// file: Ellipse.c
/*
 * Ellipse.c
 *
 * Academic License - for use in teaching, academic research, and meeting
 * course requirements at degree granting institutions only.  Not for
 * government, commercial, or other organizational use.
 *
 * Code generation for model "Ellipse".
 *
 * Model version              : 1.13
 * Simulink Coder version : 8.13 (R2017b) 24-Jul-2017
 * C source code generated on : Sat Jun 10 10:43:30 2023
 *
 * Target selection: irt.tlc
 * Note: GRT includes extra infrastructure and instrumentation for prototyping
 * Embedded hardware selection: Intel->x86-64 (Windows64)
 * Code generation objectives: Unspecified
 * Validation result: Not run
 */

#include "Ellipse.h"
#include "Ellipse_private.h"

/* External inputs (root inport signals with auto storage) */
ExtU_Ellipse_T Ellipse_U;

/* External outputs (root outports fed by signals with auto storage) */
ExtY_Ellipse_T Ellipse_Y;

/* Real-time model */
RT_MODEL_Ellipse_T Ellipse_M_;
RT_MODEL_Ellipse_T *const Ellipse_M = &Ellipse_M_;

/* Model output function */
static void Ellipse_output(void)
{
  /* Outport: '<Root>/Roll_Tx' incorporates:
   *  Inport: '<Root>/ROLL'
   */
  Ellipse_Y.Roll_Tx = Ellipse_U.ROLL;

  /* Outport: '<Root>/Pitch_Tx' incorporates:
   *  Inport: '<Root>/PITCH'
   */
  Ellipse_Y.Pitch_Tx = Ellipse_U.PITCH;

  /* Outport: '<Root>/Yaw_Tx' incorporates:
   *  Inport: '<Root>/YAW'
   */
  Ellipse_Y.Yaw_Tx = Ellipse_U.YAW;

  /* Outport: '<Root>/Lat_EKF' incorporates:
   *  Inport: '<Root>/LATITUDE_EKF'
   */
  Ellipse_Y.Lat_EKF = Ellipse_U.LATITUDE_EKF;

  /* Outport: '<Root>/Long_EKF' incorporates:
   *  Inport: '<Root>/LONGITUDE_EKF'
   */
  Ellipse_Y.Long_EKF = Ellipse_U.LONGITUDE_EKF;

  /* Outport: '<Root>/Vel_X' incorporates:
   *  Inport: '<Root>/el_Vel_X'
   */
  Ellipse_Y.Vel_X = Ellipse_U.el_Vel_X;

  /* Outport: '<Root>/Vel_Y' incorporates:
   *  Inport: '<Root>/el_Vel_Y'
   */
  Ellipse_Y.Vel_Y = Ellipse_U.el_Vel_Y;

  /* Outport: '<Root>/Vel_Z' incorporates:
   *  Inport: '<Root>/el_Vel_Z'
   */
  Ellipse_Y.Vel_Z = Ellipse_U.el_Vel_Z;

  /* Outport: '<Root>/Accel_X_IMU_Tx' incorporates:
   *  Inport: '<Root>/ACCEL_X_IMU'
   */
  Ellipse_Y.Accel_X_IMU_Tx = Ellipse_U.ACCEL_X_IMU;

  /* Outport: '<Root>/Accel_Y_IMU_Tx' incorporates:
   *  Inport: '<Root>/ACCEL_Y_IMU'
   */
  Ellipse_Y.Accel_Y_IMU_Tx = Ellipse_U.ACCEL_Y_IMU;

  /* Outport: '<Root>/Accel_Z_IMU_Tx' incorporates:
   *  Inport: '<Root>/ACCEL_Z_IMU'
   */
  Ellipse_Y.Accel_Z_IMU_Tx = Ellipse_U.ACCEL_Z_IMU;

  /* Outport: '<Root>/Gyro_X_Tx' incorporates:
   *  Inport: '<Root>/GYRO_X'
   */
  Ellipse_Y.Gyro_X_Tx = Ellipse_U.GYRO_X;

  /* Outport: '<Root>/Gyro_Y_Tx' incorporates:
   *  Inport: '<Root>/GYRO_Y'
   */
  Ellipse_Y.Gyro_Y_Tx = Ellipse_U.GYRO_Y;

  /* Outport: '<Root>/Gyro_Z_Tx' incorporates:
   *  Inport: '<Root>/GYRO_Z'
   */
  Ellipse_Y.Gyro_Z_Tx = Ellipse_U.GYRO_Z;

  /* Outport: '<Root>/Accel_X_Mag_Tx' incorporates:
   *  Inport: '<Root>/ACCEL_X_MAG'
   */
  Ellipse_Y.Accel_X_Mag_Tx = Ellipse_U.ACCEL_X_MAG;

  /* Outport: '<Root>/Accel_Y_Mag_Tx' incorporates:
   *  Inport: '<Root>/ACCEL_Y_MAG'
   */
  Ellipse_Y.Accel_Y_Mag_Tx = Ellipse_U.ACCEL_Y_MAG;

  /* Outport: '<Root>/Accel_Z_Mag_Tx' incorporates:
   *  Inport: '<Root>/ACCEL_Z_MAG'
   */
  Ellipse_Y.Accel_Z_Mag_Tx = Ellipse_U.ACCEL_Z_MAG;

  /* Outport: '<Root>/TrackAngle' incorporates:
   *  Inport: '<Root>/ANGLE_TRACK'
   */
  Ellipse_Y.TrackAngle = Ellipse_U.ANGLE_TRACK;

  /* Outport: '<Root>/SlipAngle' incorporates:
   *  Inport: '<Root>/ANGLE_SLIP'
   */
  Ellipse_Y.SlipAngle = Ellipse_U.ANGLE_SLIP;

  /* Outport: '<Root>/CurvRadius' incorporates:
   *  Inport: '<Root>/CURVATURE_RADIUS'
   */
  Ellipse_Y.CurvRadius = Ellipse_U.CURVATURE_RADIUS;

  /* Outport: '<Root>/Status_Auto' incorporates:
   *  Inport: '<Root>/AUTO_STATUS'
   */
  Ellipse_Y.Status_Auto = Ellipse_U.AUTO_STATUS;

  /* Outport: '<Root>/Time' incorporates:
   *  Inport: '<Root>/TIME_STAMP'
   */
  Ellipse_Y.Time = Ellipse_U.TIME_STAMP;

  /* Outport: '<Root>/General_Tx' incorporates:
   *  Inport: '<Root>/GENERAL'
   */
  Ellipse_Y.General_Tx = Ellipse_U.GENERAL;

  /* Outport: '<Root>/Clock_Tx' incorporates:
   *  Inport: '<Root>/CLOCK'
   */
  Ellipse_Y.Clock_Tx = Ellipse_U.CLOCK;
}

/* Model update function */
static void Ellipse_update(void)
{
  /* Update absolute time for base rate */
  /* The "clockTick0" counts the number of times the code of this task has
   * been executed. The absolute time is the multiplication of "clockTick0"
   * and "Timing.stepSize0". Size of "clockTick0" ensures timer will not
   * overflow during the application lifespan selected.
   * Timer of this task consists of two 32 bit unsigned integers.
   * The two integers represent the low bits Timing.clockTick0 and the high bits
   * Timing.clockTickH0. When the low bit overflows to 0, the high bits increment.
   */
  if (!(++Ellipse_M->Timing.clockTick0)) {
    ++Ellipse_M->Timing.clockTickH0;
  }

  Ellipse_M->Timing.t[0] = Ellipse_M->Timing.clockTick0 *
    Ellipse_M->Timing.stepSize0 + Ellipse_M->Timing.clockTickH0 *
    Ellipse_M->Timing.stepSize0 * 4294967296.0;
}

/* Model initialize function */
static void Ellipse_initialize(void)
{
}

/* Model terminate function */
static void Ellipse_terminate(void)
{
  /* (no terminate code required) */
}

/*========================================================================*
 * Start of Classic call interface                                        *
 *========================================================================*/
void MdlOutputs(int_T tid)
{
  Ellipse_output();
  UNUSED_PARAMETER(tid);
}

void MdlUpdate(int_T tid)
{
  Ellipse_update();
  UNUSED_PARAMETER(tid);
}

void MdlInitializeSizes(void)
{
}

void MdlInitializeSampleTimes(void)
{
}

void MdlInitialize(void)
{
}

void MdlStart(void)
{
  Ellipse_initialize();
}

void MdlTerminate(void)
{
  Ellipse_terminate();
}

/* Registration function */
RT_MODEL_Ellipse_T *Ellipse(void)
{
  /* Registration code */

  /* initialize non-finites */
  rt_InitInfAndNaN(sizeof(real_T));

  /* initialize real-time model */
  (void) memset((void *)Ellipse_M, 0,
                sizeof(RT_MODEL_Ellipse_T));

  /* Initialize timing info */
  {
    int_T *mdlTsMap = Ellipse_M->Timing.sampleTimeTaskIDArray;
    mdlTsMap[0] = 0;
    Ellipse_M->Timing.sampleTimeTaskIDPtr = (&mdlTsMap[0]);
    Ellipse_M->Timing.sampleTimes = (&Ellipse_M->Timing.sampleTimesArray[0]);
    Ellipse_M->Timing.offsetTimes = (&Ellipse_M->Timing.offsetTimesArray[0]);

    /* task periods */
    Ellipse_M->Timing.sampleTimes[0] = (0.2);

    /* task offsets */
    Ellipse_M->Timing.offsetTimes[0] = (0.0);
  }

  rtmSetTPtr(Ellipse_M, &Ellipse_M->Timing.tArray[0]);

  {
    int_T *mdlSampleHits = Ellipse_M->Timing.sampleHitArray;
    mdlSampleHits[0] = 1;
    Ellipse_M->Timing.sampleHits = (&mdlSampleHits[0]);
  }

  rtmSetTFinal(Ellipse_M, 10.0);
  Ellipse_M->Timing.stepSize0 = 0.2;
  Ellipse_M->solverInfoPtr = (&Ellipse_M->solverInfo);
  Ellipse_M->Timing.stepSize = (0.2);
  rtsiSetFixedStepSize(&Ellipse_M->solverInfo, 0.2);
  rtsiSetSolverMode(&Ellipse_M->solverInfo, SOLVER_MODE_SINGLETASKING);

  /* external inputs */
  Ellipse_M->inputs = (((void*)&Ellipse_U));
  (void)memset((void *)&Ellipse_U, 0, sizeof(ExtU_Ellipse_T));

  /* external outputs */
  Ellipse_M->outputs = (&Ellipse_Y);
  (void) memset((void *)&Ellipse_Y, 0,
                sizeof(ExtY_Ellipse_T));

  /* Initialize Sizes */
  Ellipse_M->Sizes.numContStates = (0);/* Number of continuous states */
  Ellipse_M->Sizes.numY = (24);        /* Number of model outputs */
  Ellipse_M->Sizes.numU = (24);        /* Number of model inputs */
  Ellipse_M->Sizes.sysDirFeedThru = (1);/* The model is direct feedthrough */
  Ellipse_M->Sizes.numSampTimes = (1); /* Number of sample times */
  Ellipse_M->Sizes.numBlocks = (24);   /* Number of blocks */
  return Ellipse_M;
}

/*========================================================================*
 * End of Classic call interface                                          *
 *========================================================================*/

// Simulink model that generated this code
simulink model "Ellipse"  (R2017b)
settings: Solver=FixedStepAuto  StartTime=0.0  StopTime=10.0  RelTol=1e-3

== system Ellipse ==
  ROLL : Inport
  PITCH : Inport  Port=2
  YAW : Inport  Port=3
  LATITUDE_EKF : Inport  Port=4
  LONGITUDE_EKF : Inport  Port=5
  el_Vel_X : Inport  Port=6
  el_Vel_Y : Inport  Port=7
  el_Vel_Z : Inport  Port=8
  ACCEL_X_IMU : Inport  Port=9
  ACCEL_Y_IMU : Inport  Port=10
  ACCEL_Z_IMU : Inport  Port=11
  GYRO_X : Inport  Port=12
  GYRO_Y : Inport  Port=13
  GYRO_Z : Inport  Port=14
  ACCEL_X_MAG : Inport  Port=15
  ACCEL_Y_MAG : Inport  Port=16
  ACCEL_Z_MAG : Inport  Port=17
  ANGLE_TRACK : Inport  Port=18
  ANGLE_SLIP : Inport  Port=19
  CURVATURE_RADIUS : Inport  Port=20
  AUTO_STATUS : Inport  Port=21
  TIME_STAMP : Inport  Port=22
  GENERAL : Inport  Port=23
  CLOCK : Inport  Port=24
  Roll_Tx : Outport
  Pitch_Tx : Outport  Port=2
  Yaw_Tx : Outport  Port=3
  Lat_EKF : Outport  Port=4
  Long_EKF : Outport  Port=5
  Vel_X : Outport  Port=6
  Vel_Y : Outport  Port=7
  Vel_Z : Outport  Port=8
  Accel_X_IMU_Tx : Outport  Port=9
  Accel_Y_IMU_Tx : Outport  Port=10
  Accel_Z_IMU_Tx : Outport  Port=11
  Gyro_X_Tx : Outport  Port=12
  Gyro_Y_Tx : Outport  Port=13
  Gyro_Z_Tx : Outport  Port=14
  Accel_X_Mag_Tx : Outport  Port=15
  Accel_Y_Mag_Tx : Outport  Port=16
  Accel_Z_Mag_Tx : Outport  Port=17
  TrackAngle : Outport  Port=18
  SlipAngle : Outport  Port=19
  CurvRadius : Outport  Port=20
  Status_Auto : Outport  Port=21
  Time : Outport  Port=22
  General_Tx : Outport  Port=23
  Clock_Tx : Outport  Port=24
  wires:
  CLOCK/1 -> Clock_Tx/1
  GENERAL/1 -> General_Tx/1
  TIME_STAMP/1 -> Time/1
  AUTO_STATUS/1 -> Status_Auto/1
  CURVATURE_RADIUS/1 -> CurvRadius/1
  ANGLE_SLIP/1 -> SlipAngle/1
  ANGLE_TRACK/1 -> TrackAngle/1
  ACCEL_Z_MAG/1 -> Accel_Z_Mag_Tx/1
  ACCEL_Y_MAG/1 -> Accel_Y_Mag_Tx/1
  ACCEL_X_MAG/1 -> Accel_X_Mag_Tx/1
  GYRO_Z/1 -> Gyro_Z_Tx/1
  GYRO_Y/1 -> Gyro_Y_Tx/1
  GYRO_X/1 -> Gyro_X_Tx/1
  ACCEL_Z_IMU/1 -> Accel_Z_IMU_Tx/1
  ACCEL_Y_IMU/1 -> Accel_Y_IMU_Tx/1
  ACCEL_X_IMU/1 -> Accel_X_IMU_Tx/1
  el_Vel_Z/1 -> Vel_Z/1
  el_Vel_Y/1 -> Vel_Y/1
  el_Vel_X/1 -> Vel_X/1
  LONGITUDE_EKF/1 -> Long_EKF/1
  LATITUDE_EKF/1 -> Lat_EKF/1
  YAW/1 -> Yaw_Tx/1
  PITCH/1 -> Pitch_Tx/1
  ROLL/1 -> Roll_Tx/1
